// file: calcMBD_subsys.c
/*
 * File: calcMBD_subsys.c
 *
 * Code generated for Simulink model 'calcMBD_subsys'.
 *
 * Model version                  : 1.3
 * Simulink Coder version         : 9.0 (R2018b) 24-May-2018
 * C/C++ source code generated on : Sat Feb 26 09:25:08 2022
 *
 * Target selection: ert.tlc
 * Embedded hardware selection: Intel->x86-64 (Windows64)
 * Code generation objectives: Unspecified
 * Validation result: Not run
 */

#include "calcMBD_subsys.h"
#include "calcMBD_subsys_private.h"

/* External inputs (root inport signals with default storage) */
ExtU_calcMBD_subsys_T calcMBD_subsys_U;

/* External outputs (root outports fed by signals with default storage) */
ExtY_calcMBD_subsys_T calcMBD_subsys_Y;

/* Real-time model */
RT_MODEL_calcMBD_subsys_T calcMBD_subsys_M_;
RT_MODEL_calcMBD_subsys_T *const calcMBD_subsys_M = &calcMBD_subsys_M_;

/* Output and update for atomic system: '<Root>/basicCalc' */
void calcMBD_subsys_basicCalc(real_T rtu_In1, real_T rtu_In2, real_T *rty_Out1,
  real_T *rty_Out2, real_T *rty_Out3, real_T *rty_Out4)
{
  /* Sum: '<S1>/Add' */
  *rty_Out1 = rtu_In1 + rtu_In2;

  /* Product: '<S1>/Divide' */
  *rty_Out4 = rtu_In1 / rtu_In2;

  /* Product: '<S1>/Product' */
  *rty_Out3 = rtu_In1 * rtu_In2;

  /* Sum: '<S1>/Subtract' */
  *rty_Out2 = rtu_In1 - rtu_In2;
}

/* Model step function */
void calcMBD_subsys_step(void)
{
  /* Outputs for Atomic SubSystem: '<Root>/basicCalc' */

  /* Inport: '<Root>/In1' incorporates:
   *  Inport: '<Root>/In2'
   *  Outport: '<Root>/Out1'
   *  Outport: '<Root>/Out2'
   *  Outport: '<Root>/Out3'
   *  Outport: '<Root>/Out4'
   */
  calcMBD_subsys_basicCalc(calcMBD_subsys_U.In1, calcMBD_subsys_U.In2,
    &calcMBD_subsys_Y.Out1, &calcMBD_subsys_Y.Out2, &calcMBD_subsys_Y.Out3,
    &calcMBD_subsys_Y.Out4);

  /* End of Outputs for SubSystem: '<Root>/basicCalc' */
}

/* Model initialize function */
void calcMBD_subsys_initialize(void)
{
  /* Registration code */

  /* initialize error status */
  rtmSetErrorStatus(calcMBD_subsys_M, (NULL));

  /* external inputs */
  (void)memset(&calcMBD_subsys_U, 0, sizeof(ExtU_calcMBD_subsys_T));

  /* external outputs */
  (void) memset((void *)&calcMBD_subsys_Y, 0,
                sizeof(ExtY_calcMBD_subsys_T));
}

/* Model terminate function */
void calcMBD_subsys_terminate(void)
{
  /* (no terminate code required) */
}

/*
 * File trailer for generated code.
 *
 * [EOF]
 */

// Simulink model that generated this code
simulink model "calcMBD_subsys"  (R2018b)
settings: Solver=FixedStepDiscrete  StartTime=0.0  StopTime=10.0  RelTol=1e-3

== system calcMBD_subsys ==
  In1 : Inport
  In2 : Inport  Port=2
  basicCalc : Subsystem  TreatAsAtomicUnit=on
  Out1 : Outport
  Out2 : Outport  Port=2
  Out3 : Outport  Port=3
  Out4 : Outport  Port=4
  wires:
  In1/1 -> basicCalc/1(In1)
  In2/1 -> basicCalc/2(In2)
  basicCalc/1(Out1) -> Out1/1
  basicCalc/2(Out2) -> Out2/1
  basicCalc/3(Out3) -> Out3/1
  basicCalc/4(Out4) -> Out4/1

== system calcMBD_subsys/basicCalc ==
  In1 : Inport
  In2 : Inport  Port=2
  Add : Sum
  Divide : Product  Inputs=*/
  Product : Product
  Subtract : Sum  Inputs=+-
  Out1 : Outport
  Out2 : Outport  Port=2
  Out3 : Outport  Port=3
  Out4 : Outport  Port=4
  wires:
  Product/1 -> Out3/1
  In1/1 -> Divide/1, Product/1, Subtract/1, Add/1
  Subtract/1 -> Out2/1
  In2/1 -> Divide/2, Product/2, Add/2, Subtract/2
  Add/1 -> Out1/1
  Divide/1 -> Out4/1
